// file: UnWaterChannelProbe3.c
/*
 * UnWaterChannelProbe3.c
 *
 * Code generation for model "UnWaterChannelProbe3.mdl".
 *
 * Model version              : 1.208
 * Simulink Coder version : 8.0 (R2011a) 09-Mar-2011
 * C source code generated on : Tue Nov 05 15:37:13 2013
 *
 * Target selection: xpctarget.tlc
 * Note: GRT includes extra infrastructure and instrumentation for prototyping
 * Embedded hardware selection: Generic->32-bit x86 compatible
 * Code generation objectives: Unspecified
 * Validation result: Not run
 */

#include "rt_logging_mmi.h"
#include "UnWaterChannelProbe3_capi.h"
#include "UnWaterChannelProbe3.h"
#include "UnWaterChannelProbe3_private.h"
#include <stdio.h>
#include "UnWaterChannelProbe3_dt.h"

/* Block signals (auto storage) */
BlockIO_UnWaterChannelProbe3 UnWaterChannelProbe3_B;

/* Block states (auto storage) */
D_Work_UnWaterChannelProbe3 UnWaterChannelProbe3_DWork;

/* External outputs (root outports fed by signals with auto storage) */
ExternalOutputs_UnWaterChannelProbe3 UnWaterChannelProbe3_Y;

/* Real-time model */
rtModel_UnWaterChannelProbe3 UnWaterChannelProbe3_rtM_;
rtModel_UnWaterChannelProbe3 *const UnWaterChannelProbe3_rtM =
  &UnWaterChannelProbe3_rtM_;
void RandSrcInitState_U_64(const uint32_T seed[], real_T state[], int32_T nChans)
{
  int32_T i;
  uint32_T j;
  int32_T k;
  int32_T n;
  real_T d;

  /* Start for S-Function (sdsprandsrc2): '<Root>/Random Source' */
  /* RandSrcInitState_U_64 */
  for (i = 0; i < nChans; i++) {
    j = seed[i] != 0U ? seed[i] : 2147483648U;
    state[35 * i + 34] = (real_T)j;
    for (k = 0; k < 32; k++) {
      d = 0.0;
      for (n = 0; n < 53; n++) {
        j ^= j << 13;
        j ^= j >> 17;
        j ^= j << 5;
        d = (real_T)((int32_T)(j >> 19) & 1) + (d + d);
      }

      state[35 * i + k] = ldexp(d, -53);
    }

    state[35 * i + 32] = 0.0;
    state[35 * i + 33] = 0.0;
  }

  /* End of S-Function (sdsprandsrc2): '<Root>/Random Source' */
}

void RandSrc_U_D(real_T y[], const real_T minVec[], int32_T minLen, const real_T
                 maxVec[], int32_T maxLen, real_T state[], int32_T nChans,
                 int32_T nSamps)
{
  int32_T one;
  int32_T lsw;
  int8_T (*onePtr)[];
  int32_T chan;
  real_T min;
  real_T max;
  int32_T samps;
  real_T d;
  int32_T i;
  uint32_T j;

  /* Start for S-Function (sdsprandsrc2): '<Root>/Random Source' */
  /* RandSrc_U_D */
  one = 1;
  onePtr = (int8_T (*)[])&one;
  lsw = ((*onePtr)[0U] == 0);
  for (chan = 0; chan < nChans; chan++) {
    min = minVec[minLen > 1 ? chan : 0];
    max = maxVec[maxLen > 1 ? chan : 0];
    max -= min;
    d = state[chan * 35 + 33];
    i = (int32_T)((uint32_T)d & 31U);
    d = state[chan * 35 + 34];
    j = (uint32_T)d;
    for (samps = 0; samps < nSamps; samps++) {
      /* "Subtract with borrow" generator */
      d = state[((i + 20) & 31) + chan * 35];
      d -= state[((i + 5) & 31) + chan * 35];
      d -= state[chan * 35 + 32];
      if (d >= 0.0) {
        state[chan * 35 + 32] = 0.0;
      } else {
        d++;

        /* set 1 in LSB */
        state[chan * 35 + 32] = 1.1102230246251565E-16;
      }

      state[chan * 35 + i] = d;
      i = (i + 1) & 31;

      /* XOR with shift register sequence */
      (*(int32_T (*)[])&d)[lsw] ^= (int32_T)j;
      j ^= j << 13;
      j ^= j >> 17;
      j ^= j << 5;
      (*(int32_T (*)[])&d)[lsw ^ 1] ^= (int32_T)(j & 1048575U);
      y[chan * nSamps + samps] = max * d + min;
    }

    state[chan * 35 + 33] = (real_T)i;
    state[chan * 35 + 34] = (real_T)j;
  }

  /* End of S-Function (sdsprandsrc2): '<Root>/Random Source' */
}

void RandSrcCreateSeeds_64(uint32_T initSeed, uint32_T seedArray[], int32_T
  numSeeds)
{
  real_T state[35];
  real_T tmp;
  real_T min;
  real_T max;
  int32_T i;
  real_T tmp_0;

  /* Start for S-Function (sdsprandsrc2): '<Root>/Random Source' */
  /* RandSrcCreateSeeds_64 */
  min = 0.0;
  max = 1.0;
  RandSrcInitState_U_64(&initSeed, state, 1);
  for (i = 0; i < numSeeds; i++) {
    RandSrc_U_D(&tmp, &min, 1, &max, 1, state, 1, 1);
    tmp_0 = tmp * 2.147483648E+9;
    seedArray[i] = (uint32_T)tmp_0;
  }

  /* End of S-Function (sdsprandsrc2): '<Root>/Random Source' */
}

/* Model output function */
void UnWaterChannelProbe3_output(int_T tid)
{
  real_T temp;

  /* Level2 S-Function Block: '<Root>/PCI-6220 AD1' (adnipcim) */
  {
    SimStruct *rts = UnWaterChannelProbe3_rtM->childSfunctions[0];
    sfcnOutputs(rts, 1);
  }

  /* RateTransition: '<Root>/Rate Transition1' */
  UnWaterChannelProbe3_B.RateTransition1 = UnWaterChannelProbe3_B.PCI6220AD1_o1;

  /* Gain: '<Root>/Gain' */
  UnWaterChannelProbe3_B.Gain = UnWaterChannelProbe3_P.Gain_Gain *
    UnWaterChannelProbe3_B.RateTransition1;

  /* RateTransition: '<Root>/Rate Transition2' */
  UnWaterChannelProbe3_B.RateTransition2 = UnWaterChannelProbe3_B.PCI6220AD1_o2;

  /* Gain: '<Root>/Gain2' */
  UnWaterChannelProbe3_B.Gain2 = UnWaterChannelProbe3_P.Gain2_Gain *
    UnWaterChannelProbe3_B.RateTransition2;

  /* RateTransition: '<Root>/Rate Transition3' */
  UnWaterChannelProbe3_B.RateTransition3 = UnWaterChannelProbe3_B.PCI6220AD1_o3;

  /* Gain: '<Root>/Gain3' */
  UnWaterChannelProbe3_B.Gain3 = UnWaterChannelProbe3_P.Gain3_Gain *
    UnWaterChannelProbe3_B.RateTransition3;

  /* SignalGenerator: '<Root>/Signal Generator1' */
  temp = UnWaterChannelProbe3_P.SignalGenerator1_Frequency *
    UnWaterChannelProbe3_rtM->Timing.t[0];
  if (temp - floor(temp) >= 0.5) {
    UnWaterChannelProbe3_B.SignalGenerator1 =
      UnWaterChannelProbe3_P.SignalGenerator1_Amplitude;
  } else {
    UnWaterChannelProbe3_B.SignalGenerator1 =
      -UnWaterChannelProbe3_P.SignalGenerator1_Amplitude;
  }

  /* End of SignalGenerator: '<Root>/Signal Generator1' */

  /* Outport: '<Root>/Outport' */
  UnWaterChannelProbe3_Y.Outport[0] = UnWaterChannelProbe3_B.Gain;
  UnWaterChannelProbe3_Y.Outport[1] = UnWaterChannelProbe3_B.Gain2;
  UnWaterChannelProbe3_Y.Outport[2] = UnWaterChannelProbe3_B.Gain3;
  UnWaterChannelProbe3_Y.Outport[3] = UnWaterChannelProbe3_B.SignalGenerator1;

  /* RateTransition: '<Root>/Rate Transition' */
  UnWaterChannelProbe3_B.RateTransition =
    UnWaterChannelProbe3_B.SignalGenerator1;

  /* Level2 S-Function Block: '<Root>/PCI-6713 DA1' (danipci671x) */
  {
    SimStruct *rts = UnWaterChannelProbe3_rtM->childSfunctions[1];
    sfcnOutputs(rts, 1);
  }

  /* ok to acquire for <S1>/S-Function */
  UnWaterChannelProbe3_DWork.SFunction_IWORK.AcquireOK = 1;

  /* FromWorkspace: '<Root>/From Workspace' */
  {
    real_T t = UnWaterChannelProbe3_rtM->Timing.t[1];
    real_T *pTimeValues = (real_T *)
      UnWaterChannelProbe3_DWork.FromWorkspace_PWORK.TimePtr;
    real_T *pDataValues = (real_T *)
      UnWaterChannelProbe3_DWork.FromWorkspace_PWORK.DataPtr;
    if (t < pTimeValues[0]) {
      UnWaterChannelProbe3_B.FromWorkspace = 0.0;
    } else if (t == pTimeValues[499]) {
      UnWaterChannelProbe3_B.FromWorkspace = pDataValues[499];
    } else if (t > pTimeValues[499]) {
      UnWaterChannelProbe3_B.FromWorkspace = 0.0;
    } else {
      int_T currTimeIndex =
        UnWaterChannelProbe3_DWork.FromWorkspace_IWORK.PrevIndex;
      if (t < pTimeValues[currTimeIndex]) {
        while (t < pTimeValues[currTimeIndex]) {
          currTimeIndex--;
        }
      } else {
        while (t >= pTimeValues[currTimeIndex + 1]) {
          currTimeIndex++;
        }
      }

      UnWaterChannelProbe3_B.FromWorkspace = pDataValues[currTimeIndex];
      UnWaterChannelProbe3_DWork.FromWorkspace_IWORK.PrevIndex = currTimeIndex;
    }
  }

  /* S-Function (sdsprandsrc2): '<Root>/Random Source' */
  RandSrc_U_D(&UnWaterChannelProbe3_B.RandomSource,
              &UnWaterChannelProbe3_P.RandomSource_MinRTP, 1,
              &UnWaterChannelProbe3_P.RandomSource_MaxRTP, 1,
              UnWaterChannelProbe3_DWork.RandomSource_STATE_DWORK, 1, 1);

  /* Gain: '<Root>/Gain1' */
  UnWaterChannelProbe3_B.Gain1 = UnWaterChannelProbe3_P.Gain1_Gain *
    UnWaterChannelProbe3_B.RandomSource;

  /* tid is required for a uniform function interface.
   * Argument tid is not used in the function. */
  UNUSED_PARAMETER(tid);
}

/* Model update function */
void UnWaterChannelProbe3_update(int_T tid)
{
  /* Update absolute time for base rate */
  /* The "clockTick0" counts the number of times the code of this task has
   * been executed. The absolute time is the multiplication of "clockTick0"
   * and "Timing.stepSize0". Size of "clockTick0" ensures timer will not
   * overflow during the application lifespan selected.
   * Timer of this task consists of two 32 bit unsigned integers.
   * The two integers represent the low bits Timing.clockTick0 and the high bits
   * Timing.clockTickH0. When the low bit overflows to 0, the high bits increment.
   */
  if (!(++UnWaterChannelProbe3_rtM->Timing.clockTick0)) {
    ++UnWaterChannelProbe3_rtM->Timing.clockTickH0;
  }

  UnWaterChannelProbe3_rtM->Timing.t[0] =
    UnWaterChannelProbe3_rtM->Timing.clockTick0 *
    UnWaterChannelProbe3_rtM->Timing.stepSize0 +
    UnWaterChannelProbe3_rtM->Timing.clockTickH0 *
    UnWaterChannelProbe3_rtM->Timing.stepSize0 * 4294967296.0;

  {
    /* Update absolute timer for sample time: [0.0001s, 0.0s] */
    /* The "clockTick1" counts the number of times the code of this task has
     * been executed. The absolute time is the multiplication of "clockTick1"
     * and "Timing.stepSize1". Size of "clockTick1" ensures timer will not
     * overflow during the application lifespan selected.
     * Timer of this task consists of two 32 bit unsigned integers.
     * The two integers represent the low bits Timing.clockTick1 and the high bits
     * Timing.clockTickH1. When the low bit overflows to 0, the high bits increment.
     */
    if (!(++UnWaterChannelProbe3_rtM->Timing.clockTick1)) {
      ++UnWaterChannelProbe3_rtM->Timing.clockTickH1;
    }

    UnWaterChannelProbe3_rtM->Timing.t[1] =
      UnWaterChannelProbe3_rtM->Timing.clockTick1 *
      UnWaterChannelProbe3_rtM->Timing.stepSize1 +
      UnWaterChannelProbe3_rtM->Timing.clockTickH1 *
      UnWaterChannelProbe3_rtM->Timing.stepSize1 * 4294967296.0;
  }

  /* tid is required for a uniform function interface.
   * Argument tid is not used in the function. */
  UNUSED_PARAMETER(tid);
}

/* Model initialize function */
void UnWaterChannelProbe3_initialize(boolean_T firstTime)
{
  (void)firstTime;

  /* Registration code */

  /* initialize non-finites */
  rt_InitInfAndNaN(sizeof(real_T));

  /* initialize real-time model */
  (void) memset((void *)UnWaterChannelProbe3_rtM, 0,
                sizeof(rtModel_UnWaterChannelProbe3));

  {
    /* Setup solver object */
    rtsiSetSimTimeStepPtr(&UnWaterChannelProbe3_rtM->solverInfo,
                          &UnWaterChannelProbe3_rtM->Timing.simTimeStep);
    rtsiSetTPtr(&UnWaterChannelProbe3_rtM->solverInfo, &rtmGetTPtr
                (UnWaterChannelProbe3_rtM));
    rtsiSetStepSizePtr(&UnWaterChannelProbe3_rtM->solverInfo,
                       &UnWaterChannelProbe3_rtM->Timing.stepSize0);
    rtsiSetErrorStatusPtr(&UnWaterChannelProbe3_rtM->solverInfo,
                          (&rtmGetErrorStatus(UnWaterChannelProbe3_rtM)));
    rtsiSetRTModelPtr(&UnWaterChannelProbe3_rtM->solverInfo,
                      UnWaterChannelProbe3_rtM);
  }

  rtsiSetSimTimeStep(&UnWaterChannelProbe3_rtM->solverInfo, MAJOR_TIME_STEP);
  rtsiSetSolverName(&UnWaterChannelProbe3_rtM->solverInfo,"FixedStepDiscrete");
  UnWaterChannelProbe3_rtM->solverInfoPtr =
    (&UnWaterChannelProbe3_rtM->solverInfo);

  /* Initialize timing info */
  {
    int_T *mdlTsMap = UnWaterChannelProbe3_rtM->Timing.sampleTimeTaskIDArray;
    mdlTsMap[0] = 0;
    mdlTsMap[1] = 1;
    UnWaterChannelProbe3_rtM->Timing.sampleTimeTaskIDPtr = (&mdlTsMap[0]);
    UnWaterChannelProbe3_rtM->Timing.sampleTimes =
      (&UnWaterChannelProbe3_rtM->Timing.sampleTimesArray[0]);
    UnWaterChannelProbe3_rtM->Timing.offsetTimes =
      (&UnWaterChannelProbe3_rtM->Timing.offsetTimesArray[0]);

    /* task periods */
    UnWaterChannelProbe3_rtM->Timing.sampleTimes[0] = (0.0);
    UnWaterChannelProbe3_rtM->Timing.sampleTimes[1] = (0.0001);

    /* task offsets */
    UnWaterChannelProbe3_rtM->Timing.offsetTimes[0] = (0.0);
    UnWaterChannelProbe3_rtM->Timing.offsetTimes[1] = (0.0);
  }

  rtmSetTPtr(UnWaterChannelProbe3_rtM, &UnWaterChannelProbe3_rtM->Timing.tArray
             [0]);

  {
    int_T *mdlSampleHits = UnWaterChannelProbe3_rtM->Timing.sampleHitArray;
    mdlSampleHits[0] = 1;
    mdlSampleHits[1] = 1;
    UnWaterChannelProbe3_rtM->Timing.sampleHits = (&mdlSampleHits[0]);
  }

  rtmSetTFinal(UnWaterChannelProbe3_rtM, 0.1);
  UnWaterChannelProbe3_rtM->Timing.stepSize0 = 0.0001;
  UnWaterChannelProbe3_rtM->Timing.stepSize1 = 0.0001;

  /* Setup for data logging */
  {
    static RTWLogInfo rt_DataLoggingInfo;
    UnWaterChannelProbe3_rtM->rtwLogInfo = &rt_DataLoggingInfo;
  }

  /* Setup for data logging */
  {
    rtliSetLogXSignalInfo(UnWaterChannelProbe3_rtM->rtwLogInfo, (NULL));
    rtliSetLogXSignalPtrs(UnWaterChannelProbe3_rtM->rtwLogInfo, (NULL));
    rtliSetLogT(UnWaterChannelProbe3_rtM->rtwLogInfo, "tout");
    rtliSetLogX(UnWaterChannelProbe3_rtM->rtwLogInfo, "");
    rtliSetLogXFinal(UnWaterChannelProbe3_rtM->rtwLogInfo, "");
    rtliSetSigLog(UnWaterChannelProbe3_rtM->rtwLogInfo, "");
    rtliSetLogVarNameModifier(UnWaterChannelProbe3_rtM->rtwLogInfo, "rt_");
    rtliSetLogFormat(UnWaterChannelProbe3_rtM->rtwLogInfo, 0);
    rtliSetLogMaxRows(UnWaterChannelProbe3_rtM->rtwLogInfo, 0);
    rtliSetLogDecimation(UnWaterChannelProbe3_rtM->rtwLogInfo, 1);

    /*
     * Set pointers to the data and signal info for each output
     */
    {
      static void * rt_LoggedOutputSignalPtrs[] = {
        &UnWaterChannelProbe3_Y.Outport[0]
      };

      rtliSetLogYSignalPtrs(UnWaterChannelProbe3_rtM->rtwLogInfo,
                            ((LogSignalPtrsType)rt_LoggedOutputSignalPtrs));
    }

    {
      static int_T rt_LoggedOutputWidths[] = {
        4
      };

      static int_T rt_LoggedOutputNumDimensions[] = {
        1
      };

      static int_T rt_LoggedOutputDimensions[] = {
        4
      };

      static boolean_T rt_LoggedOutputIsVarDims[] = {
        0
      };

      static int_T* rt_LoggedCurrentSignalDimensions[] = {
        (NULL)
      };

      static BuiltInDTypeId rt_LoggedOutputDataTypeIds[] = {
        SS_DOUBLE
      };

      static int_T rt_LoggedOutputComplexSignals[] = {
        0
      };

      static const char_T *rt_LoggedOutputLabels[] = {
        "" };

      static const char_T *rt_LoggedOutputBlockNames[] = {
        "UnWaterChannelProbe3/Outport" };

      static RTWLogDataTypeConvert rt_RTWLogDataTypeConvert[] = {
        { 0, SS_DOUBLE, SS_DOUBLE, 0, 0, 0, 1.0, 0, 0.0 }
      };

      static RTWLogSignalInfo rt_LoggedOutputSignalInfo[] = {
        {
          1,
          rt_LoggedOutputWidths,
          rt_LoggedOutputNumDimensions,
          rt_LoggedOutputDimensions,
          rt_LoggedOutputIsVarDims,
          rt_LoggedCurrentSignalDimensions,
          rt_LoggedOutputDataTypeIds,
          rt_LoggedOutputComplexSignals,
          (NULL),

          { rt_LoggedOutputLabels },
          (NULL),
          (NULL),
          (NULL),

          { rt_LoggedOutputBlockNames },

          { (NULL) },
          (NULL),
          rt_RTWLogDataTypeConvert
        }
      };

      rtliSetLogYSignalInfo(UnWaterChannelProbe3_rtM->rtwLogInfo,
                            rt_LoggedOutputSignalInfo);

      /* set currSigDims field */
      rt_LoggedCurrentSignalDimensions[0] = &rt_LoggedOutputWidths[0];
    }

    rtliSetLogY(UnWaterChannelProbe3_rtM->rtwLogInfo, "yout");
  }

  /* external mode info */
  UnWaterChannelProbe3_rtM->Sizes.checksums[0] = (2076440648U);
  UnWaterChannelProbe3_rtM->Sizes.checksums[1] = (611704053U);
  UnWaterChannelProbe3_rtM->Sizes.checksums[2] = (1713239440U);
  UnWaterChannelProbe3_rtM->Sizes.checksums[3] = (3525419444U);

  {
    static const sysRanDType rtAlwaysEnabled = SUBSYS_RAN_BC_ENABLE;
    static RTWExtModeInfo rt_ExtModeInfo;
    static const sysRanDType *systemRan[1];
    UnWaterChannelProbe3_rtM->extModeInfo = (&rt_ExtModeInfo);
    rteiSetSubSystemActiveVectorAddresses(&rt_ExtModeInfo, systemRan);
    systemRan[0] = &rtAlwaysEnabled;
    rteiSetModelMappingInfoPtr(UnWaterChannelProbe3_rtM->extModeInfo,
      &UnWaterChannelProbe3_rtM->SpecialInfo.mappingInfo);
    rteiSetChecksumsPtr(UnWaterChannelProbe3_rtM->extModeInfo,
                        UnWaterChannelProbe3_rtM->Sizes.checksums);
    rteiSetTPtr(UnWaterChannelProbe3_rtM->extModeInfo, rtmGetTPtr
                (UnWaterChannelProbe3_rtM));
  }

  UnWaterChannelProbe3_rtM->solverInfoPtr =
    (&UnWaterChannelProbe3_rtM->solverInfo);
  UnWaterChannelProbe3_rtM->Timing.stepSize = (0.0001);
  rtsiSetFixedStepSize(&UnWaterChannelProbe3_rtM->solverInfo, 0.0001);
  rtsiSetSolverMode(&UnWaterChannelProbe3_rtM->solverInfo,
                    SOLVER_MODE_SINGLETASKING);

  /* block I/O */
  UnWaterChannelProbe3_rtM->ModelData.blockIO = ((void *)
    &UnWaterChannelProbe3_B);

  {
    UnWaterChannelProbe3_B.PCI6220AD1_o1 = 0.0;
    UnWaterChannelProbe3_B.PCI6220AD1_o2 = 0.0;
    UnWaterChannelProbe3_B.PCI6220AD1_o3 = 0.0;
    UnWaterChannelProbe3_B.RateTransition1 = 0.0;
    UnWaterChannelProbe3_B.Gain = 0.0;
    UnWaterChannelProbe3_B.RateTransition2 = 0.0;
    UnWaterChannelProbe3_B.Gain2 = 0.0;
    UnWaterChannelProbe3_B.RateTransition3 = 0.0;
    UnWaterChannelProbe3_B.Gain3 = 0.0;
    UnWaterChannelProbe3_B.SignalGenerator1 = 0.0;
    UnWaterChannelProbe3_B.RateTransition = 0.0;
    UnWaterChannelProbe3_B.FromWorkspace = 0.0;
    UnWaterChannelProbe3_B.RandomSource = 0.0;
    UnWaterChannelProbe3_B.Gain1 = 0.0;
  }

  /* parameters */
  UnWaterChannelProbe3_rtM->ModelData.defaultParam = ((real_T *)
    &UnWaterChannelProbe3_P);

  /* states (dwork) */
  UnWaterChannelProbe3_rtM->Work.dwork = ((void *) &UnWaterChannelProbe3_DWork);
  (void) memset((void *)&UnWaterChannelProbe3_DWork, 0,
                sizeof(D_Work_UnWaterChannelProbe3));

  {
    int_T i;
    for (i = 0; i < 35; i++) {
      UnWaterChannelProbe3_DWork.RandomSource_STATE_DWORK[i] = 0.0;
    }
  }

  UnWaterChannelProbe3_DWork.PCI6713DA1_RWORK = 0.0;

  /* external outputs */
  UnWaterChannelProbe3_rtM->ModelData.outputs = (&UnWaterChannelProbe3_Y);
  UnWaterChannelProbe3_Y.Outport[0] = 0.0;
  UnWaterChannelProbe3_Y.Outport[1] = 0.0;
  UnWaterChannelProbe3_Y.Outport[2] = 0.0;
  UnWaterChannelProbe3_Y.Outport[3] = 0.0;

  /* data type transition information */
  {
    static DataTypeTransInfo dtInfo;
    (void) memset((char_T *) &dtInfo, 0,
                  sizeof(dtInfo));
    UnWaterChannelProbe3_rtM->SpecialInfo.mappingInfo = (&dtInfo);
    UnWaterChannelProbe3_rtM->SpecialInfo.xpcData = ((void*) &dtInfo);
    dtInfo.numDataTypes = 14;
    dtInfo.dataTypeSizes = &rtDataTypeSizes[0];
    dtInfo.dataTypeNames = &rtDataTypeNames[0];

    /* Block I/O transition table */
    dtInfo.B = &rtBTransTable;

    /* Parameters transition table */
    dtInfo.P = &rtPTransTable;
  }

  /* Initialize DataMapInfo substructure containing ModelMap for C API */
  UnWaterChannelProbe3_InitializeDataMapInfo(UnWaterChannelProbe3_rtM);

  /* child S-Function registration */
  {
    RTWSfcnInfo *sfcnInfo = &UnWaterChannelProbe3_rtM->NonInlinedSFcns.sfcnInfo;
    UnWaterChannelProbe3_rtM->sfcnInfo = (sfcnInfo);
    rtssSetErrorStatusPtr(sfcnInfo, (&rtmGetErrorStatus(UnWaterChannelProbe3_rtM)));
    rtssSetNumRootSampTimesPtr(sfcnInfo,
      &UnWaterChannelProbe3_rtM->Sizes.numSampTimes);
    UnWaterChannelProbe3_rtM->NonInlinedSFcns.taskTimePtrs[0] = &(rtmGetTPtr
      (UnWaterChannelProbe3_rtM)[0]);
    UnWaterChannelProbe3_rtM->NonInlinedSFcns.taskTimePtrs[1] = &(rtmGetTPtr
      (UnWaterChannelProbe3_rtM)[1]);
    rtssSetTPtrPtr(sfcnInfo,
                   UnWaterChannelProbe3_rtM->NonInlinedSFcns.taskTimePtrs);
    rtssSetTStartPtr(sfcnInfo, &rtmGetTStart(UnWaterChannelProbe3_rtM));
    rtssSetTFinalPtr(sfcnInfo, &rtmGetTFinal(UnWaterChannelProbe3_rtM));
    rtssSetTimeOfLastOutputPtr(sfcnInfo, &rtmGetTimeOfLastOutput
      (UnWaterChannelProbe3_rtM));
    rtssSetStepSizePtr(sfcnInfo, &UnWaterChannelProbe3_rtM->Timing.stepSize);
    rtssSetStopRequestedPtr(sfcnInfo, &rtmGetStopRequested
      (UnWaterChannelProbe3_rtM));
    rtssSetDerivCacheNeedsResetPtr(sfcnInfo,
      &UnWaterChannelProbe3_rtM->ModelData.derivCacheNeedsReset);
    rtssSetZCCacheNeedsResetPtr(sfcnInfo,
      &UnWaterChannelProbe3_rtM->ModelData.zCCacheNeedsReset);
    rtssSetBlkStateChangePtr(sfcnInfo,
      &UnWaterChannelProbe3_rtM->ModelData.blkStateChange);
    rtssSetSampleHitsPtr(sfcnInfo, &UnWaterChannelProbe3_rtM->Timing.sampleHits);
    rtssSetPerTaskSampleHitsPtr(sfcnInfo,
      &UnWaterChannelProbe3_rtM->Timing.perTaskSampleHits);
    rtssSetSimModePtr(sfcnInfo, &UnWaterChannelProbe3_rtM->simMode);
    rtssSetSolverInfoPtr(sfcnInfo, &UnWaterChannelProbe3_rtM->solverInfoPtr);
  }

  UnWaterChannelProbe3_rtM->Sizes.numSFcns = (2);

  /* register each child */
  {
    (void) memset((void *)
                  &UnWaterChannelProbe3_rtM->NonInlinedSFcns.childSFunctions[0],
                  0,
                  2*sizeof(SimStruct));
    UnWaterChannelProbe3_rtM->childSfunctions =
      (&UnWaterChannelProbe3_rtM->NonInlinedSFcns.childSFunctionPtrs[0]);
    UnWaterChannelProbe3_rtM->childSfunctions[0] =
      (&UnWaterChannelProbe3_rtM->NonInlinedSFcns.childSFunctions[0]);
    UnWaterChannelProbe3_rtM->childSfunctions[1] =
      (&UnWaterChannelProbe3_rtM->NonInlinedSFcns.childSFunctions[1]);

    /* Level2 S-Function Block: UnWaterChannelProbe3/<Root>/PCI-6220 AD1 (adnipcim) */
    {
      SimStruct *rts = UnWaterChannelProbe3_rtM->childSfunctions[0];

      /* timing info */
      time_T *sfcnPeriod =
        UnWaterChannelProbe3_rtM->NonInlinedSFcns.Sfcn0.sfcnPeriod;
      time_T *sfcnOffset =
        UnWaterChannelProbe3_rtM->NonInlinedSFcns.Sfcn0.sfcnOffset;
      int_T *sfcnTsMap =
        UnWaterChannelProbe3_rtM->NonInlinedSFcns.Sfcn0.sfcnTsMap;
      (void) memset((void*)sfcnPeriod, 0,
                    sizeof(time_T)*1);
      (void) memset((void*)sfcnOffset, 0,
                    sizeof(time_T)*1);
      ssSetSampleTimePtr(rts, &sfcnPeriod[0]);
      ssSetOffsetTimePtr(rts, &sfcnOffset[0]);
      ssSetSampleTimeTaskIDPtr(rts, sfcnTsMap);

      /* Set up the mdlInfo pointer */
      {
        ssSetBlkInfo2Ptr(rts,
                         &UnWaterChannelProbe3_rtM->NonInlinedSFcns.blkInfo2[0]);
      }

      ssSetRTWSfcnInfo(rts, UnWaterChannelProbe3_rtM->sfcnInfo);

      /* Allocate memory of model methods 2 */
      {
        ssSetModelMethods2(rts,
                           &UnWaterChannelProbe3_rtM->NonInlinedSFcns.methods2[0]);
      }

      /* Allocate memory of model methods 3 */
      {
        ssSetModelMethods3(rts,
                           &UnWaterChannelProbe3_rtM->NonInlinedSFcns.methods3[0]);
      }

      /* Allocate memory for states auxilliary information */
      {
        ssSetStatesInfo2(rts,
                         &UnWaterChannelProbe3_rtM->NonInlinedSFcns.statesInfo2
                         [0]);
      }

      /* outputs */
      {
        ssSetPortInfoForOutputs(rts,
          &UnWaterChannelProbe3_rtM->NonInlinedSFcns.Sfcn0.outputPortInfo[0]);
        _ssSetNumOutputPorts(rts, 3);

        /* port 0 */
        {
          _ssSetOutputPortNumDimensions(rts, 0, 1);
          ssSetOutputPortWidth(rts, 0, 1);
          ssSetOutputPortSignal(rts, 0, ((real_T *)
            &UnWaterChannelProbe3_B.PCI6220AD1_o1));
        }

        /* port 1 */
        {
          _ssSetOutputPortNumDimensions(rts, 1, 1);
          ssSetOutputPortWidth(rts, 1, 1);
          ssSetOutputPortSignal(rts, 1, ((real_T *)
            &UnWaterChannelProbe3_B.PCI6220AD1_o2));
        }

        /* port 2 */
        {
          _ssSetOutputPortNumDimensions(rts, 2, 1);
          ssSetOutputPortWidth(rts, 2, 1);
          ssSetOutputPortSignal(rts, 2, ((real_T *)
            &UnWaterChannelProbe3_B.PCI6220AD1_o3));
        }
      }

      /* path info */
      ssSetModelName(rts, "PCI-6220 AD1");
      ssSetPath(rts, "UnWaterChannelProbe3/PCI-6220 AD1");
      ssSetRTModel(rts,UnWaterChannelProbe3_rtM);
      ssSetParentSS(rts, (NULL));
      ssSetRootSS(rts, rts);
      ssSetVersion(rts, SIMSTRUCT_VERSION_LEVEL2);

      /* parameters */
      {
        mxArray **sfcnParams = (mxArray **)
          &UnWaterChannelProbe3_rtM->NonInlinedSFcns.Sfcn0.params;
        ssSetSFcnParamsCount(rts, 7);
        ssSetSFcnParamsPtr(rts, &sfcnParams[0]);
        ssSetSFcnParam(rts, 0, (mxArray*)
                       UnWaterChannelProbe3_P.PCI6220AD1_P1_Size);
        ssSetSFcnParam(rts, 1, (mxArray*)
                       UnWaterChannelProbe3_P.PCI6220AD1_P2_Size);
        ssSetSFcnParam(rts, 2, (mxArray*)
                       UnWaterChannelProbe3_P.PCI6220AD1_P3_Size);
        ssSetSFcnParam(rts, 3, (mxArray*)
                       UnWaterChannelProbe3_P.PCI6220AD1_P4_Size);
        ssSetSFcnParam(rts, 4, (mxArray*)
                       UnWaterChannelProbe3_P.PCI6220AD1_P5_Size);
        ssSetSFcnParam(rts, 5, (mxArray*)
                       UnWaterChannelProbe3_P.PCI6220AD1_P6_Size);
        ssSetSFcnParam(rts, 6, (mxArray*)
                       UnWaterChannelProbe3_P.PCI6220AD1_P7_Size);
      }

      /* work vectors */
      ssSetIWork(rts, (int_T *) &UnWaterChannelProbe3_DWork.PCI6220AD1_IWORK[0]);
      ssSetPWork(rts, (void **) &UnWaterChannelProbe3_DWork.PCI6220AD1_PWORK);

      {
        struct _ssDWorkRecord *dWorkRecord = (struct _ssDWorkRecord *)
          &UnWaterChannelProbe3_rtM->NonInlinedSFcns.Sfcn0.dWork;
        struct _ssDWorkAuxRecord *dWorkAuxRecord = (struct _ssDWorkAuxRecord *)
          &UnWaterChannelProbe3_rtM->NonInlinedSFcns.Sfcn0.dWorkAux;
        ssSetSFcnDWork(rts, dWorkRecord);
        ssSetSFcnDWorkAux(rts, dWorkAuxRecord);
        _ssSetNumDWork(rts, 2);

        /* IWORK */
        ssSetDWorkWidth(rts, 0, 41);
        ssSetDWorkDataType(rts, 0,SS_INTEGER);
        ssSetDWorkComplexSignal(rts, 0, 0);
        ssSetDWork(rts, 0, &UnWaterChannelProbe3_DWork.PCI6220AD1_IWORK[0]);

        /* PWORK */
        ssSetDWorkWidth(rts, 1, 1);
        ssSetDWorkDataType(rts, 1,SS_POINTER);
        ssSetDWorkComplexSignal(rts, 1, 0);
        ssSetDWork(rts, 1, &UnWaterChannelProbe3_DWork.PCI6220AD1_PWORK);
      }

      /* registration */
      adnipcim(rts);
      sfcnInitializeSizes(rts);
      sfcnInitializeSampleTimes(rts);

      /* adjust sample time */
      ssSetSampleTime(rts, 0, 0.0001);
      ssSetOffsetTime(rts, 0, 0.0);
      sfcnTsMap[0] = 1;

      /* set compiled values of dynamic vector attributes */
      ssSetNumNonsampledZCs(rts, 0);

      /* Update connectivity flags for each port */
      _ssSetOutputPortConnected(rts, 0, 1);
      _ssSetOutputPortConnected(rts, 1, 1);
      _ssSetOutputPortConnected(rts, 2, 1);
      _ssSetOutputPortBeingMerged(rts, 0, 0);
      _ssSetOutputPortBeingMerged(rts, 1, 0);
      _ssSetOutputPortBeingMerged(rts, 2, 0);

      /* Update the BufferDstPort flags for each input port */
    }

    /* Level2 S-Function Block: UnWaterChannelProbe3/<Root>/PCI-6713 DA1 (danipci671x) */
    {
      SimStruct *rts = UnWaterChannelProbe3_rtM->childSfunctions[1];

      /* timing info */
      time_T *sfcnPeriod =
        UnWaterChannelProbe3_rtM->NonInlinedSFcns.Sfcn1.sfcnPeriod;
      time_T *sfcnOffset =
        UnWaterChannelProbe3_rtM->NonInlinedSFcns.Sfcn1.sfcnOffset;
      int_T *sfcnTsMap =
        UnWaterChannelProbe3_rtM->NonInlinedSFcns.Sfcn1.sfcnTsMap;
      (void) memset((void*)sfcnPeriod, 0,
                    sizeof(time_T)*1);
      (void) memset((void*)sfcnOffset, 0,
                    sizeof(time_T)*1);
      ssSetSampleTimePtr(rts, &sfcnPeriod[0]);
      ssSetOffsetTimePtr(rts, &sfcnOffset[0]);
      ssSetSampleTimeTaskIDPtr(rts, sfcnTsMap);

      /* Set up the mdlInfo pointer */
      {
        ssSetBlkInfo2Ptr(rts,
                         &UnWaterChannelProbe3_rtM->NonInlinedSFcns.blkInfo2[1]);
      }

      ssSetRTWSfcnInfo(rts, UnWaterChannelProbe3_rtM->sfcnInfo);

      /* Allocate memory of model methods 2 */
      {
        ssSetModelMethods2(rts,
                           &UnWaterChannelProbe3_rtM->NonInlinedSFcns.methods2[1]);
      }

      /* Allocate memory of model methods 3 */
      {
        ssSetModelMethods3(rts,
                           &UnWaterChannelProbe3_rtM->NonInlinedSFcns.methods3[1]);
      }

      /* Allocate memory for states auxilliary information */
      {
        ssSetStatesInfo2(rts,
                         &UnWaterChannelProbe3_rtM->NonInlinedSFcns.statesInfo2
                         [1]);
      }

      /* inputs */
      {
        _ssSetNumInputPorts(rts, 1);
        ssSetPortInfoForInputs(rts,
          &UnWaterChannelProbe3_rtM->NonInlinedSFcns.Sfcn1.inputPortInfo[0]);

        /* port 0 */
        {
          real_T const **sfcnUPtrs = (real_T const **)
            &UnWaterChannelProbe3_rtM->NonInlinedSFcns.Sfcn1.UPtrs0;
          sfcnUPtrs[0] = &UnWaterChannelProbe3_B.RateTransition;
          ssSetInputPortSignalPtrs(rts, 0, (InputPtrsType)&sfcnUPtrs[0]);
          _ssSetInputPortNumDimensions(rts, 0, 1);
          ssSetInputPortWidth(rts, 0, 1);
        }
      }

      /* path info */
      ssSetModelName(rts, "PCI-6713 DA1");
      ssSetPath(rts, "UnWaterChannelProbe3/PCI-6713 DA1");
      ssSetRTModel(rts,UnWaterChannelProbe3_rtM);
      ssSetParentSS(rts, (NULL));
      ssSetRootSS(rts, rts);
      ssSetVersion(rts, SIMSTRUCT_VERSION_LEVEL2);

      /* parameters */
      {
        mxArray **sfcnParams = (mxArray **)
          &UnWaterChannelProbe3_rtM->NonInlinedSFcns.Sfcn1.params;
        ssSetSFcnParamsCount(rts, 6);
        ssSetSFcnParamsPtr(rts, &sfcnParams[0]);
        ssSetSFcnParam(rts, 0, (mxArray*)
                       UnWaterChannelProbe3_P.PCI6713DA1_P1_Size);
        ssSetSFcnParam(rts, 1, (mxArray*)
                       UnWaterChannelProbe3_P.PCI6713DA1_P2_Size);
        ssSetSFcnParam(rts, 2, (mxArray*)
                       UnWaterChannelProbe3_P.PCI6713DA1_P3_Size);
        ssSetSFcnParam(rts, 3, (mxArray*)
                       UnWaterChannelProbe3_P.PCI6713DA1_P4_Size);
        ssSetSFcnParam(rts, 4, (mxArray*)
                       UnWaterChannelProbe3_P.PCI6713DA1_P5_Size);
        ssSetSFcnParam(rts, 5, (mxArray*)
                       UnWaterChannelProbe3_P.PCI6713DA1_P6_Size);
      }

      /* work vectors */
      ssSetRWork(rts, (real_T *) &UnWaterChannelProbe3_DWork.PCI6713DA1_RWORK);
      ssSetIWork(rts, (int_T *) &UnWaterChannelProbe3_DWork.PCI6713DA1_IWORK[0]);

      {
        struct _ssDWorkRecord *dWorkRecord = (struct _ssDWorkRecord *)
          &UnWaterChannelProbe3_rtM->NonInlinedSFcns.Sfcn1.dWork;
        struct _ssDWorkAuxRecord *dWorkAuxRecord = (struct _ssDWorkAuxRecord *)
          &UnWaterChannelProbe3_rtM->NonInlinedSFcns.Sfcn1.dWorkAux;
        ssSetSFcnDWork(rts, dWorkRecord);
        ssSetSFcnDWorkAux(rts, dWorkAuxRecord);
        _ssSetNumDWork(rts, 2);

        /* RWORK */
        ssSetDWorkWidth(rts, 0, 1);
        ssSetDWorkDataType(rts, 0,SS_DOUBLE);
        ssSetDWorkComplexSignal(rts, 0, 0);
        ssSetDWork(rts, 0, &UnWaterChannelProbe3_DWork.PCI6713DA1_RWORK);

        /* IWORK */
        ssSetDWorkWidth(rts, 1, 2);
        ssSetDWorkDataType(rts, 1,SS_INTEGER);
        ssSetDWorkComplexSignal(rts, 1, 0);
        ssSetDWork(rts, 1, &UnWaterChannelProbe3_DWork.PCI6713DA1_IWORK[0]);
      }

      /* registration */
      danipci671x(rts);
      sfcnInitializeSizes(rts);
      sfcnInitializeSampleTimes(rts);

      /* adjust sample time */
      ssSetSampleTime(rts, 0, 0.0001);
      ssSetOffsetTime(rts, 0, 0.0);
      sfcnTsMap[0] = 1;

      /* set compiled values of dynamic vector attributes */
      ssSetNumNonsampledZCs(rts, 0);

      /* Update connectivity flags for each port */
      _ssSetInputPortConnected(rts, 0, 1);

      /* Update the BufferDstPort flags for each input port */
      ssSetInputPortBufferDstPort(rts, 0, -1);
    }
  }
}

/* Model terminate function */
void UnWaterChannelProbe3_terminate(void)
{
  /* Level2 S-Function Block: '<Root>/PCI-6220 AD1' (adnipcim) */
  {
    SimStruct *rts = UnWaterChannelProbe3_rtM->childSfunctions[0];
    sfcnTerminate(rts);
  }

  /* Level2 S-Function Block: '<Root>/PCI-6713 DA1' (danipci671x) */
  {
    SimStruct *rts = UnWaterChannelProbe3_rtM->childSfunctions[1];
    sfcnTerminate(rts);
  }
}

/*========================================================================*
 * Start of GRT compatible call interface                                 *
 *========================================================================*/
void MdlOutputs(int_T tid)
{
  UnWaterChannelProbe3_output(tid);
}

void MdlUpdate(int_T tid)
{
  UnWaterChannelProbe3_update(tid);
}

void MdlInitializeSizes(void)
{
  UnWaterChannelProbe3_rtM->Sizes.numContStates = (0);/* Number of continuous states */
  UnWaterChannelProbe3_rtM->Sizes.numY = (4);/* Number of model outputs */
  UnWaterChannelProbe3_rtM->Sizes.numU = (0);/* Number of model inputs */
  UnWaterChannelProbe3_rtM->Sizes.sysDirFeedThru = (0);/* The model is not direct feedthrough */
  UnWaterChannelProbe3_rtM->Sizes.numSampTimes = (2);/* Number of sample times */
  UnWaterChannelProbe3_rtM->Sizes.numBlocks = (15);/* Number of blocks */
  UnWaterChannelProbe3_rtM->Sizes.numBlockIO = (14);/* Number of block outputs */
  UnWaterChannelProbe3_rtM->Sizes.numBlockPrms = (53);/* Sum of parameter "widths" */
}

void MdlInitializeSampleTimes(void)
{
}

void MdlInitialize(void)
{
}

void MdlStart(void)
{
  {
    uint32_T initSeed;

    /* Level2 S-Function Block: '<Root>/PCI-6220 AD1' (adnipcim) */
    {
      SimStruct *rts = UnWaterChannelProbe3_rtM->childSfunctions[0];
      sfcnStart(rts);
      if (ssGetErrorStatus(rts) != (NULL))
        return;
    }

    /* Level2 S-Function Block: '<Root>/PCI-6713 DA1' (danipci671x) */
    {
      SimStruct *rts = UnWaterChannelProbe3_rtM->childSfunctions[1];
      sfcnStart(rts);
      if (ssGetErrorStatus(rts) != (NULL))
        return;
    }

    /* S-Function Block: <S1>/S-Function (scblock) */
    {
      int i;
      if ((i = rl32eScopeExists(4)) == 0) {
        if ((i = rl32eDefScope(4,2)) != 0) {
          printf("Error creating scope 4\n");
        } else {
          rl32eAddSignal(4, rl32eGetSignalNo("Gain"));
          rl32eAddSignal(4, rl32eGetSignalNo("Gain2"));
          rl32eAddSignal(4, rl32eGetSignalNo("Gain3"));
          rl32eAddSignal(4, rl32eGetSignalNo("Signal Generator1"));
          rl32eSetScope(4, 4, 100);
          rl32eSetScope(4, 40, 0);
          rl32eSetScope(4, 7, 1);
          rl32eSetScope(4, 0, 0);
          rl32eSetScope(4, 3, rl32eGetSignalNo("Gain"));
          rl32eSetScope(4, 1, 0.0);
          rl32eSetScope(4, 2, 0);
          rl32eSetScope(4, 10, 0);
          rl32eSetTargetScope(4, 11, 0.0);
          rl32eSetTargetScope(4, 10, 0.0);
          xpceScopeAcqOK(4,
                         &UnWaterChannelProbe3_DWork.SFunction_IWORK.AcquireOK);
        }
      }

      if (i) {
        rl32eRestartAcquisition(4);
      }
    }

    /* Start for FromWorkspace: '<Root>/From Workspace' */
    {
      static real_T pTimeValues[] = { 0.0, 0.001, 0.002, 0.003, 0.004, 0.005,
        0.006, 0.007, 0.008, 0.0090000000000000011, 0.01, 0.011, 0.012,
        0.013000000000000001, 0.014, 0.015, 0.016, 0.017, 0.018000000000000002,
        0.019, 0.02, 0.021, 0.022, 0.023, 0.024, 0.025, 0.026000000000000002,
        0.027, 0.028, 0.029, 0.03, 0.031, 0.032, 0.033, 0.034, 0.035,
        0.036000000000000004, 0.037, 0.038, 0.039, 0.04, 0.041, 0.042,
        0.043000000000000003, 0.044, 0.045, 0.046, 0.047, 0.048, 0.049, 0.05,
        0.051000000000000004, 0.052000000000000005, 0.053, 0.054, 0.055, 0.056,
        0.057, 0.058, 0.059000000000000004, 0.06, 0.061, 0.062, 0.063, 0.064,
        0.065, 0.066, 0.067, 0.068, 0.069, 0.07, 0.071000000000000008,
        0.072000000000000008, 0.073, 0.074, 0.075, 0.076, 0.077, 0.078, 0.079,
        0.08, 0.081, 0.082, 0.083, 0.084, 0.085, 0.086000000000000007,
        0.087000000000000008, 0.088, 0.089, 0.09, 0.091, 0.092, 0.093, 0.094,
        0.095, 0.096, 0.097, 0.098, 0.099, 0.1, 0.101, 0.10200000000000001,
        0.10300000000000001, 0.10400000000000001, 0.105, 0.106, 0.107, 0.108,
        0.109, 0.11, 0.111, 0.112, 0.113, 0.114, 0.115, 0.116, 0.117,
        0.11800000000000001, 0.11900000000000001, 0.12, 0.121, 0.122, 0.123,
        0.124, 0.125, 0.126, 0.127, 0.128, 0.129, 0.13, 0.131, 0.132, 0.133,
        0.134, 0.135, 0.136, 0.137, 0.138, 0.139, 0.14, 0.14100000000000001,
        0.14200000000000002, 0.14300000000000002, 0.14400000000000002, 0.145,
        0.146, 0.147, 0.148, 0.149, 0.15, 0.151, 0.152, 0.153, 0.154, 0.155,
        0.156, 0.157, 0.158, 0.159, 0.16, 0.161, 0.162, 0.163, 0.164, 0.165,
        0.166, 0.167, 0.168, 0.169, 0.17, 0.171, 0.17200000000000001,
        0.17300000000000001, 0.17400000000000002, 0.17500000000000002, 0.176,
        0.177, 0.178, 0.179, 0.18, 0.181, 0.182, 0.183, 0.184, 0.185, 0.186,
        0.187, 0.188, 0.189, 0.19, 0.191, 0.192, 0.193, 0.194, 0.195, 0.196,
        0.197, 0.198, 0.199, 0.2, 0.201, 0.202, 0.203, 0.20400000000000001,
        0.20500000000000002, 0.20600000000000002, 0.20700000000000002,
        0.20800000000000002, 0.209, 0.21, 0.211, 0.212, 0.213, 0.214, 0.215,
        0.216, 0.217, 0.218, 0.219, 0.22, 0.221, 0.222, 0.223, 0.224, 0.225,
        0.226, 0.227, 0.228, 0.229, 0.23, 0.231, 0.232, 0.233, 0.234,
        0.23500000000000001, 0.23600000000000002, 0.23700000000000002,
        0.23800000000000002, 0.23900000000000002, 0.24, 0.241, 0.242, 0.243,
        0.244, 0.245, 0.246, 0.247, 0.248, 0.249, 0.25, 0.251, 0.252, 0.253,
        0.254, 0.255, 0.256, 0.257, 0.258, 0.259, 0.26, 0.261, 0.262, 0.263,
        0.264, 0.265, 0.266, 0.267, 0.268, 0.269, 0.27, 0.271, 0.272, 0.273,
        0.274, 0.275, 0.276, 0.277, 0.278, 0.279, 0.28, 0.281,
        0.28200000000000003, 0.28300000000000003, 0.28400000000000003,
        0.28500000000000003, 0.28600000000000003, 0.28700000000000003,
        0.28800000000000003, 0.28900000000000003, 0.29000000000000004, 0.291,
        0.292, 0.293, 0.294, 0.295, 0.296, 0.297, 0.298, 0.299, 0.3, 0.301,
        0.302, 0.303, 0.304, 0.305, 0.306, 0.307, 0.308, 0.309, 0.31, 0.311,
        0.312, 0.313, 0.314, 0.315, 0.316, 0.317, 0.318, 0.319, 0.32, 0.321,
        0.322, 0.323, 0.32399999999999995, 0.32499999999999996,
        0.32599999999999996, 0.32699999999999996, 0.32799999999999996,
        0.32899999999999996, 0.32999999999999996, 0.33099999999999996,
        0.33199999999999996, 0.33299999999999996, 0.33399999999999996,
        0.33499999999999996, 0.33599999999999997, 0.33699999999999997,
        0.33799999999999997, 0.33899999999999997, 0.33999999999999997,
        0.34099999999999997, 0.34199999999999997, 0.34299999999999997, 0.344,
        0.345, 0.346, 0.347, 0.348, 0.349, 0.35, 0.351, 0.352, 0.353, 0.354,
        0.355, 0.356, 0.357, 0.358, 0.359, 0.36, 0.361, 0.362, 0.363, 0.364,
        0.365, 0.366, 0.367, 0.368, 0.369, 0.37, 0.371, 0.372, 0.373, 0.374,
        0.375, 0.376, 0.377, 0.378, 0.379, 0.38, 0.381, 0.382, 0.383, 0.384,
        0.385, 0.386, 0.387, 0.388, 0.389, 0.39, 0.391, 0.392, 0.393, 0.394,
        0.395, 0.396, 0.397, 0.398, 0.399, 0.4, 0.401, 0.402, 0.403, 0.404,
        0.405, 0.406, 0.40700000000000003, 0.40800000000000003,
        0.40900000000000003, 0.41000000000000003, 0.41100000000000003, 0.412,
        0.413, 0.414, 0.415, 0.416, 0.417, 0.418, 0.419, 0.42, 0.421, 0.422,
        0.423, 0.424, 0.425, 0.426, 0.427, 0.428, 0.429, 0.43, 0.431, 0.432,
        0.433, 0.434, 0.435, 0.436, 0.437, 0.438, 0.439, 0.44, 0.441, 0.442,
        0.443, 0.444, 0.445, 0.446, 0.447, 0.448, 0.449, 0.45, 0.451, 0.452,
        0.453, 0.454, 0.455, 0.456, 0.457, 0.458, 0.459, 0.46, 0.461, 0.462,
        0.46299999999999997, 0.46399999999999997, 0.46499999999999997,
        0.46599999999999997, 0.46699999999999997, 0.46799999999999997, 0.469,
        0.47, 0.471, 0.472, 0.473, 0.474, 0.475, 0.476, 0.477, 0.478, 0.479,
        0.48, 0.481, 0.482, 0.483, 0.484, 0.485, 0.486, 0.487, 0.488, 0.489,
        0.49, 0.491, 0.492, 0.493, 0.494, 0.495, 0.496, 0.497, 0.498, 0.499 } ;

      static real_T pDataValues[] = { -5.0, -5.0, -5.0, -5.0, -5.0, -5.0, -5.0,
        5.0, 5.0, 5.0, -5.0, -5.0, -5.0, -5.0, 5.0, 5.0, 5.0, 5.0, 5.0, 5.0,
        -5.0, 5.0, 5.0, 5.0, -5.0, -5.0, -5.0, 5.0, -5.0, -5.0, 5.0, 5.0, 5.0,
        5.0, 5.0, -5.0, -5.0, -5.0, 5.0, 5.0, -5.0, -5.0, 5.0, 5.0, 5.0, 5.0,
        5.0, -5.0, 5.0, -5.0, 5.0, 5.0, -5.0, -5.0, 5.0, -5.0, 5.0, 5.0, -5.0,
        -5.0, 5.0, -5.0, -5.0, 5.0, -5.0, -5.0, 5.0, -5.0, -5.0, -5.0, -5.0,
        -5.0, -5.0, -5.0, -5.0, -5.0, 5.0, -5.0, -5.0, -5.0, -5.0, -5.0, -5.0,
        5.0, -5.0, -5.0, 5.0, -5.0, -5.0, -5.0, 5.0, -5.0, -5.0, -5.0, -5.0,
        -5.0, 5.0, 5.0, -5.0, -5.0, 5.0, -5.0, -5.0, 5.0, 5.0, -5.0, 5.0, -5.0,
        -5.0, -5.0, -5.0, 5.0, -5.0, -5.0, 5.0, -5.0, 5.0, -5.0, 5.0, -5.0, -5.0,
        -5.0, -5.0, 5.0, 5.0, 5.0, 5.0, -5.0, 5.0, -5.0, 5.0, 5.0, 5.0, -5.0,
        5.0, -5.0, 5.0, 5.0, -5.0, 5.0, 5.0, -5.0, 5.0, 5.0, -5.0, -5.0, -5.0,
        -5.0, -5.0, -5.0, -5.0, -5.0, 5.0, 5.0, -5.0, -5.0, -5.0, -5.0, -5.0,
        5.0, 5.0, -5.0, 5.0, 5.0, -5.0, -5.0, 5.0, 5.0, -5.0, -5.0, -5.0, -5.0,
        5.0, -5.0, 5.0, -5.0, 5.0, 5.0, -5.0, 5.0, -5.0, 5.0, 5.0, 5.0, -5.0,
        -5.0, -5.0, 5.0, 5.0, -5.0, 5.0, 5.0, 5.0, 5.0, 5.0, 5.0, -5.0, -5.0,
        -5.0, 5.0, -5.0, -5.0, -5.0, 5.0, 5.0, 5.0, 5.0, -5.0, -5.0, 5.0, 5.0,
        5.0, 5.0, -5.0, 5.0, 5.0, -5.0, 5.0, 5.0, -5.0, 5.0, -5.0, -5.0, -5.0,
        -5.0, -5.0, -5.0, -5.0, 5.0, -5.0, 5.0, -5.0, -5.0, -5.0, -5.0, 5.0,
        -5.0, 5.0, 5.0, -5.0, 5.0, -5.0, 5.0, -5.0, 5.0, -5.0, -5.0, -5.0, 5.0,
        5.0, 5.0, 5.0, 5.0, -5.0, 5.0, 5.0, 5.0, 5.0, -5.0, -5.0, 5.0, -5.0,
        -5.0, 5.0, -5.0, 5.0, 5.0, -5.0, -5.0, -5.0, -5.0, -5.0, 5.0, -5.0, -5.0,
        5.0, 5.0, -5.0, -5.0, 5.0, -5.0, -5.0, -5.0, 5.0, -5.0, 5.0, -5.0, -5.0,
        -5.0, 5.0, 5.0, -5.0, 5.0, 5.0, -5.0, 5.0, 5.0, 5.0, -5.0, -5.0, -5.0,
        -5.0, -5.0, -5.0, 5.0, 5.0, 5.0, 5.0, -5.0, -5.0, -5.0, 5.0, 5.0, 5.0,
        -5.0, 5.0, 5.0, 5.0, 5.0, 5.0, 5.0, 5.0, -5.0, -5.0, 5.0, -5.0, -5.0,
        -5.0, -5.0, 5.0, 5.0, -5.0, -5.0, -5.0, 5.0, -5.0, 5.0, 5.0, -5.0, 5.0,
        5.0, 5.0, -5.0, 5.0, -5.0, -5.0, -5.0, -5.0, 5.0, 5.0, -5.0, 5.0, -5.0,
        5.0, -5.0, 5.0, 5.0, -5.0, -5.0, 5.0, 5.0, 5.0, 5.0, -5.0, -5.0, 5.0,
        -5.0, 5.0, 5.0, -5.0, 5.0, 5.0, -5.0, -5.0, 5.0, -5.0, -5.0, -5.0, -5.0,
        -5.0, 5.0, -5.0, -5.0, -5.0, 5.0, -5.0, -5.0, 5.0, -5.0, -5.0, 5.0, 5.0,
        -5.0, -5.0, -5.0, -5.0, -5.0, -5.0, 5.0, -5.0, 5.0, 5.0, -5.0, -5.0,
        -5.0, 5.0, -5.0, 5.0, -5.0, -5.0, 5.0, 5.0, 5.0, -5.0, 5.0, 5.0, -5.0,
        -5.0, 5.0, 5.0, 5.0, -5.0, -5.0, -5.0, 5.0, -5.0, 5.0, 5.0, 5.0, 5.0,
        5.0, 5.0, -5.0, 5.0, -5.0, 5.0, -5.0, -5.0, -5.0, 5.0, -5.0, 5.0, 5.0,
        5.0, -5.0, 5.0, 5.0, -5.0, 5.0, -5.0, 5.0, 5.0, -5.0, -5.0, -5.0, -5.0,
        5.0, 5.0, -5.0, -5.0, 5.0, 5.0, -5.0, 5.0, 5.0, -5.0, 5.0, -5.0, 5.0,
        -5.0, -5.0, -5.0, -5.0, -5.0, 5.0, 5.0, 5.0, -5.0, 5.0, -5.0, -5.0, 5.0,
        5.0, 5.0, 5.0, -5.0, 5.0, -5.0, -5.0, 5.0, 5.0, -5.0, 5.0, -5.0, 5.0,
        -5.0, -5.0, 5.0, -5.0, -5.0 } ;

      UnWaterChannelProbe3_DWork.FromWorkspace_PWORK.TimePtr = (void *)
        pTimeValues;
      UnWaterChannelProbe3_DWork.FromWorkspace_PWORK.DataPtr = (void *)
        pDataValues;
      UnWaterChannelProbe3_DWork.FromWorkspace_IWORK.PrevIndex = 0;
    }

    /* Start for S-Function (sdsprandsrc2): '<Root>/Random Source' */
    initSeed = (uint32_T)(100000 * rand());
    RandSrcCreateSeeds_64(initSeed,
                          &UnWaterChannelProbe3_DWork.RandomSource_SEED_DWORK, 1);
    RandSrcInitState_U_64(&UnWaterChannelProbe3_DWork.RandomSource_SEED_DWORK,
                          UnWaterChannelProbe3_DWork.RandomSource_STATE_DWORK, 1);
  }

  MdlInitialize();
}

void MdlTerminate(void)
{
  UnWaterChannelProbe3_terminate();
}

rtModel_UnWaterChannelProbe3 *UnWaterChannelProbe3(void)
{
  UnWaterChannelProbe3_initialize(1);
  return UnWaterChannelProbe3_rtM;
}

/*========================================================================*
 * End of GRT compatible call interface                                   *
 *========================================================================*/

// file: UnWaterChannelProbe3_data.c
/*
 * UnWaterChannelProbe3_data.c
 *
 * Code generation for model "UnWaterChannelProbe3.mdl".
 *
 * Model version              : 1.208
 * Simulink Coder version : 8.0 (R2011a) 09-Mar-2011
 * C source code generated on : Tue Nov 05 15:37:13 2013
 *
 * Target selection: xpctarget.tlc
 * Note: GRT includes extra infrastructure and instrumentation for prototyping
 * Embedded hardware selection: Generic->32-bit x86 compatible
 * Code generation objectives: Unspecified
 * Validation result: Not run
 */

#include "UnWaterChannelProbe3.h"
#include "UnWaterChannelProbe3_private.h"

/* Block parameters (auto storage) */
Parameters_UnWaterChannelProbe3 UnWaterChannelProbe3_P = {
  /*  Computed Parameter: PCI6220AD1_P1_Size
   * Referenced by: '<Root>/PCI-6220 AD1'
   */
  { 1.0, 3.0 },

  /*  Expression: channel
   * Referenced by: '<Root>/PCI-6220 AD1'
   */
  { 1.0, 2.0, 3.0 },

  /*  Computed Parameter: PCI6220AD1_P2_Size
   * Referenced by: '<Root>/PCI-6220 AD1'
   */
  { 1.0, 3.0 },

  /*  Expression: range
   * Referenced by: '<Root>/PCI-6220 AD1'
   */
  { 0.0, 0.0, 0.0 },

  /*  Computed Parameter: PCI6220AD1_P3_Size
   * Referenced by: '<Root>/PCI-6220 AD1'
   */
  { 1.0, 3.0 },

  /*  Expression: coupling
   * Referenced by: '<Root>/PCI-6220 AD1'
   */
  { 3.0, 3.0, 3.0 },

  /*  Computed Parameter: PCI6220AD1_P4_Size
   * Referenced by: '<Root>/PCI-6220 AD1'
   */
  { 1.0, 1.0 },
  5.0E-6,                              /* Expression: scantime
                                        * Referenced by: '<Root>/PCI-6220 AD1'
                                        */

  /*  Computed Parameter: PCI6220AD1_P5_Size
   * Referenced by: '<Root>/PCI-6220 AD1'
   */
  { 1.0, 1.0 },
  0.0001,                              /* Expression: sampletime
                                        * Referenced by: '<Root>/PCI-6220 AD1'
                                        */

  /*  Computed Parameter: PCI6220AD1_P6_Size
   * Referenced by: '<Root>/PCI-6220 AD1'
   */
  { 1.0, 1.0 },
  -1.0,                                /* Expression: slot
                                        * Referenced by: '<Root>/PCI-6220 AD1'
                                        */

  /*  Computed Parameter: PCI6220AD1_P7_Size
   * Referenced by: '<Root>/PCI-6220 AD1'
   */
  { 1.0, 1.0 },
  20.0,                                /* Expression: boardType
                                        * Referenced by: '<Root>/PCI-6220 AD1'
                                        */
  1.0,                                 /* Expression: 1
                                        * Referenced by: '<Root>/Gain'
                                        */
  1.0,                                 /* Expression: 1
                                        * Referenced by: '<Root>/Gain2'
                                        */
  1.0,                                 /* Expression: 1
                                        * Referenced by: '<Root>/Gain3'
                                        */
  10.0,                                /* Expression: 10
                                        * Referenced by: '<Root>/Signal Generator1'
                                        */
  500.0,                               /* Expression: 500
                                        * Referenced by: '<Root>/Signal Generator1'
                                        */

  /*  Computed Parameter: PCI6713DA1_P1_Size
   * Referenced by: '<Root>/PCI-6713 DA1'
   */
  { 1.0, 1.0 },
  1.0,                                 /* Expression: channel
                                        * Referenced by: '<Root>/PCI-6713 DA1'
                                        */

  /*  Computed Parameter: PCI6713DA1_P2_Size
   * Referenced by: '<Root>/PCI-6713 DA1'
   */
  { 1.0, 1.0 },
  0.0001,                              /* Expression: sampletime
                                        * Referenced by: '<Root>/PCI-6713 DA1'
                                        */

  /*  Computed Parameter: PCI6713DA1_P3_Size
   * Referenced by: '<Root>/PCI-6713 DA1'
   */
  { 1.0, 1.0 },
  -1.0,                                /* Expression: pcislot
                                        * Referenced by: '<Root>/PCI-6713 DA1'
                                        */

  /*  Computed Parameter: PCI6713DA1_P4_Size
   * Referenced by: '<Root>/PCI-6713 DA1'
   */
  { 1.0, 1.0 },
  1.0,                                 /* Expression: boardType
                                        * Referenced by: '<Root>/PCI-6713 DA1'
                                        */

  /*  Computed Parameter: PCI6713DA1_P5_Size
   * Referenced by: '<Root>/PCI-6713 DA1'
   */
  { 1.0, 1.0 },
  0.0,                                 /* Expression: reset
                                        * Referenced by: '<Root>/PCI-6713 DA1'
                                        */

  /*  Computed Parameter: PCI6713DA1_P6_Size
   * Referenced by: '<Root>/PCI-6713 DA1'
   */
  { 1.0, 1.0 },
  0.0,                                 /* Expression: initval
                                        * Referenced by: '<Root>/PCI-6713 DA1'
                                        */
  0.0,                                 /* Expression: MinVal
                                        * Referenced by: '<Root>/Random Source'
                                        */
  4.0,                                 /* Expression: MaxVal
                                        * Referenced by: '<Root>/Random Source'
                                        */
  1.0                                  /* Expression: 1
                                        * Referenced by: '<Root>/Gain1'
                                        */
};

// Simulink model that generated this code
simulink model "UnWaterChannelProbe3"  (Simulink 7.7)
settings: Solver=ode4  StartTime=0  StopTime=0.1  FixedStep=0.0001  RelTol=1e-3
undefined symbols (not defined in the file): madnipcim
libraries: xpcnilib x1, dspsrcs4 x1, xpclib x1

== system UnWaterChannelProbe3 ==
  From Workspace : FromWorkspace  VariableName=prbs_train  SampleTime=1e-4  Interpolate=off  OutputAfterFinalValue=Setting to zero
  Gain{,1..3} (4 alike) : Gain
  Mux : Mux
  PCI-6220 AD1 : S-Function  AncestorBlock=xpcnilib/A//D/M Series/PCI-6221 AD  InitFcn=madnipcim(1);  FunctionName=adnipcim  Parameters="channel, range, coupling, scantime, sampletime, slot,  boardType"  SFunctionModules=xpcionim  EnableBusSupport=off  mask(adnipci6221){channel=[1,2,3], range=[10], coupling=[0], scantime=5e-6, sampletime=1e-4, slot=-1}
      mask prompts: channel "Channel vector (1-16):"; range "Range vector (in the set [10, 5, 1, 0.2]):"; coupling "Input coupling vector (0: RSE, 1: NRSE, 2: DIFF):"; scantime "Scan Interval:"; sampletime "Sample time:"; slot "PCI slot (-1: autosearch):"
      mask help:
      | PCI-6221
      | National Instruments
      | Analog Input
      mask init:
      | boardType=20;
      | [maskdisplay, range, coupling, scantime] = madnipcim(2,channel, range, coupling, scantime, boardType);
      | set_param( gcb, 'MaskDisplay', maskdisplay );
  PCI-6713 DA1 : xpcnilib/D//A/PCI-6713 DA  channel=[1]  reset=[0]  initval=[0]  sampletime=1e-4  pcislot=-1
  Random Source : dspsrcs4/Random Source  SrcType=Uniform  NormMethod=Ziggurat  CltLength=12  MinVal=0  MaxVal=4  MeanVal=0  VarVal=1  RepMode=Not repeatable  rawSeed=1  IsInherit=off  SampMode=Continuous  SampTime=2e-4  SampFrame=1  DataType=Double  OutComplex=Real
  Rate Transition{,1..3} (4 alike) : RateTransition
  Scope (xPC) 2 : xpclib/Misc./Scope (xPC)   SystemSampleTime=-1  scopeno=4  scopetype=Target  autostart=on  viewmode=Graphical redraw  formatstr='%15.6f'  grid=on  ylimits=[0,0]  nosamples=100  noprepostsamples=0  interleave=1  triggermode=FreeRun  triggersignal=1  triggerlevel=0.0  triggerslope=Either  triggerscope=1  triggersample=0  filename=data.dat  mode=Lazy  writesize=512  autorestart=off  dynamicfilemode=off  maxwritefilesize=512*1024^2
  Signal Generator1 : SignalGenerator  WaveForm=square  Amplitude=10  Frequency=500
  Outport : Outport  InitialOutput=0
  wires:
  Rate Transition/1 -> PCI-6713 DA1/1
  PCI-6220 AD1/1 -> Rate Transition1/1
  Mux/1 -> Scope (xPC) 2/1, Outport/1
  Rate Transition1/1 -> Gain/1
  Random Source/1 -> Gain1/1
  Rate Transition2/1 -> Gain2/1
  PCI-6220 AD1/2 -> Rate Transition2/1
  Gain/1 -> Mux/1
  Gain2/1 -> Mux/2
  Rate Transition3/1 -> Gain3/1
  Gain3/1 -> Mux/3
  PCI-6220 AD1/3 -> Rate Transition3/1
  Signal Generator1/1 -> Rate Transition/1, Mux/4
